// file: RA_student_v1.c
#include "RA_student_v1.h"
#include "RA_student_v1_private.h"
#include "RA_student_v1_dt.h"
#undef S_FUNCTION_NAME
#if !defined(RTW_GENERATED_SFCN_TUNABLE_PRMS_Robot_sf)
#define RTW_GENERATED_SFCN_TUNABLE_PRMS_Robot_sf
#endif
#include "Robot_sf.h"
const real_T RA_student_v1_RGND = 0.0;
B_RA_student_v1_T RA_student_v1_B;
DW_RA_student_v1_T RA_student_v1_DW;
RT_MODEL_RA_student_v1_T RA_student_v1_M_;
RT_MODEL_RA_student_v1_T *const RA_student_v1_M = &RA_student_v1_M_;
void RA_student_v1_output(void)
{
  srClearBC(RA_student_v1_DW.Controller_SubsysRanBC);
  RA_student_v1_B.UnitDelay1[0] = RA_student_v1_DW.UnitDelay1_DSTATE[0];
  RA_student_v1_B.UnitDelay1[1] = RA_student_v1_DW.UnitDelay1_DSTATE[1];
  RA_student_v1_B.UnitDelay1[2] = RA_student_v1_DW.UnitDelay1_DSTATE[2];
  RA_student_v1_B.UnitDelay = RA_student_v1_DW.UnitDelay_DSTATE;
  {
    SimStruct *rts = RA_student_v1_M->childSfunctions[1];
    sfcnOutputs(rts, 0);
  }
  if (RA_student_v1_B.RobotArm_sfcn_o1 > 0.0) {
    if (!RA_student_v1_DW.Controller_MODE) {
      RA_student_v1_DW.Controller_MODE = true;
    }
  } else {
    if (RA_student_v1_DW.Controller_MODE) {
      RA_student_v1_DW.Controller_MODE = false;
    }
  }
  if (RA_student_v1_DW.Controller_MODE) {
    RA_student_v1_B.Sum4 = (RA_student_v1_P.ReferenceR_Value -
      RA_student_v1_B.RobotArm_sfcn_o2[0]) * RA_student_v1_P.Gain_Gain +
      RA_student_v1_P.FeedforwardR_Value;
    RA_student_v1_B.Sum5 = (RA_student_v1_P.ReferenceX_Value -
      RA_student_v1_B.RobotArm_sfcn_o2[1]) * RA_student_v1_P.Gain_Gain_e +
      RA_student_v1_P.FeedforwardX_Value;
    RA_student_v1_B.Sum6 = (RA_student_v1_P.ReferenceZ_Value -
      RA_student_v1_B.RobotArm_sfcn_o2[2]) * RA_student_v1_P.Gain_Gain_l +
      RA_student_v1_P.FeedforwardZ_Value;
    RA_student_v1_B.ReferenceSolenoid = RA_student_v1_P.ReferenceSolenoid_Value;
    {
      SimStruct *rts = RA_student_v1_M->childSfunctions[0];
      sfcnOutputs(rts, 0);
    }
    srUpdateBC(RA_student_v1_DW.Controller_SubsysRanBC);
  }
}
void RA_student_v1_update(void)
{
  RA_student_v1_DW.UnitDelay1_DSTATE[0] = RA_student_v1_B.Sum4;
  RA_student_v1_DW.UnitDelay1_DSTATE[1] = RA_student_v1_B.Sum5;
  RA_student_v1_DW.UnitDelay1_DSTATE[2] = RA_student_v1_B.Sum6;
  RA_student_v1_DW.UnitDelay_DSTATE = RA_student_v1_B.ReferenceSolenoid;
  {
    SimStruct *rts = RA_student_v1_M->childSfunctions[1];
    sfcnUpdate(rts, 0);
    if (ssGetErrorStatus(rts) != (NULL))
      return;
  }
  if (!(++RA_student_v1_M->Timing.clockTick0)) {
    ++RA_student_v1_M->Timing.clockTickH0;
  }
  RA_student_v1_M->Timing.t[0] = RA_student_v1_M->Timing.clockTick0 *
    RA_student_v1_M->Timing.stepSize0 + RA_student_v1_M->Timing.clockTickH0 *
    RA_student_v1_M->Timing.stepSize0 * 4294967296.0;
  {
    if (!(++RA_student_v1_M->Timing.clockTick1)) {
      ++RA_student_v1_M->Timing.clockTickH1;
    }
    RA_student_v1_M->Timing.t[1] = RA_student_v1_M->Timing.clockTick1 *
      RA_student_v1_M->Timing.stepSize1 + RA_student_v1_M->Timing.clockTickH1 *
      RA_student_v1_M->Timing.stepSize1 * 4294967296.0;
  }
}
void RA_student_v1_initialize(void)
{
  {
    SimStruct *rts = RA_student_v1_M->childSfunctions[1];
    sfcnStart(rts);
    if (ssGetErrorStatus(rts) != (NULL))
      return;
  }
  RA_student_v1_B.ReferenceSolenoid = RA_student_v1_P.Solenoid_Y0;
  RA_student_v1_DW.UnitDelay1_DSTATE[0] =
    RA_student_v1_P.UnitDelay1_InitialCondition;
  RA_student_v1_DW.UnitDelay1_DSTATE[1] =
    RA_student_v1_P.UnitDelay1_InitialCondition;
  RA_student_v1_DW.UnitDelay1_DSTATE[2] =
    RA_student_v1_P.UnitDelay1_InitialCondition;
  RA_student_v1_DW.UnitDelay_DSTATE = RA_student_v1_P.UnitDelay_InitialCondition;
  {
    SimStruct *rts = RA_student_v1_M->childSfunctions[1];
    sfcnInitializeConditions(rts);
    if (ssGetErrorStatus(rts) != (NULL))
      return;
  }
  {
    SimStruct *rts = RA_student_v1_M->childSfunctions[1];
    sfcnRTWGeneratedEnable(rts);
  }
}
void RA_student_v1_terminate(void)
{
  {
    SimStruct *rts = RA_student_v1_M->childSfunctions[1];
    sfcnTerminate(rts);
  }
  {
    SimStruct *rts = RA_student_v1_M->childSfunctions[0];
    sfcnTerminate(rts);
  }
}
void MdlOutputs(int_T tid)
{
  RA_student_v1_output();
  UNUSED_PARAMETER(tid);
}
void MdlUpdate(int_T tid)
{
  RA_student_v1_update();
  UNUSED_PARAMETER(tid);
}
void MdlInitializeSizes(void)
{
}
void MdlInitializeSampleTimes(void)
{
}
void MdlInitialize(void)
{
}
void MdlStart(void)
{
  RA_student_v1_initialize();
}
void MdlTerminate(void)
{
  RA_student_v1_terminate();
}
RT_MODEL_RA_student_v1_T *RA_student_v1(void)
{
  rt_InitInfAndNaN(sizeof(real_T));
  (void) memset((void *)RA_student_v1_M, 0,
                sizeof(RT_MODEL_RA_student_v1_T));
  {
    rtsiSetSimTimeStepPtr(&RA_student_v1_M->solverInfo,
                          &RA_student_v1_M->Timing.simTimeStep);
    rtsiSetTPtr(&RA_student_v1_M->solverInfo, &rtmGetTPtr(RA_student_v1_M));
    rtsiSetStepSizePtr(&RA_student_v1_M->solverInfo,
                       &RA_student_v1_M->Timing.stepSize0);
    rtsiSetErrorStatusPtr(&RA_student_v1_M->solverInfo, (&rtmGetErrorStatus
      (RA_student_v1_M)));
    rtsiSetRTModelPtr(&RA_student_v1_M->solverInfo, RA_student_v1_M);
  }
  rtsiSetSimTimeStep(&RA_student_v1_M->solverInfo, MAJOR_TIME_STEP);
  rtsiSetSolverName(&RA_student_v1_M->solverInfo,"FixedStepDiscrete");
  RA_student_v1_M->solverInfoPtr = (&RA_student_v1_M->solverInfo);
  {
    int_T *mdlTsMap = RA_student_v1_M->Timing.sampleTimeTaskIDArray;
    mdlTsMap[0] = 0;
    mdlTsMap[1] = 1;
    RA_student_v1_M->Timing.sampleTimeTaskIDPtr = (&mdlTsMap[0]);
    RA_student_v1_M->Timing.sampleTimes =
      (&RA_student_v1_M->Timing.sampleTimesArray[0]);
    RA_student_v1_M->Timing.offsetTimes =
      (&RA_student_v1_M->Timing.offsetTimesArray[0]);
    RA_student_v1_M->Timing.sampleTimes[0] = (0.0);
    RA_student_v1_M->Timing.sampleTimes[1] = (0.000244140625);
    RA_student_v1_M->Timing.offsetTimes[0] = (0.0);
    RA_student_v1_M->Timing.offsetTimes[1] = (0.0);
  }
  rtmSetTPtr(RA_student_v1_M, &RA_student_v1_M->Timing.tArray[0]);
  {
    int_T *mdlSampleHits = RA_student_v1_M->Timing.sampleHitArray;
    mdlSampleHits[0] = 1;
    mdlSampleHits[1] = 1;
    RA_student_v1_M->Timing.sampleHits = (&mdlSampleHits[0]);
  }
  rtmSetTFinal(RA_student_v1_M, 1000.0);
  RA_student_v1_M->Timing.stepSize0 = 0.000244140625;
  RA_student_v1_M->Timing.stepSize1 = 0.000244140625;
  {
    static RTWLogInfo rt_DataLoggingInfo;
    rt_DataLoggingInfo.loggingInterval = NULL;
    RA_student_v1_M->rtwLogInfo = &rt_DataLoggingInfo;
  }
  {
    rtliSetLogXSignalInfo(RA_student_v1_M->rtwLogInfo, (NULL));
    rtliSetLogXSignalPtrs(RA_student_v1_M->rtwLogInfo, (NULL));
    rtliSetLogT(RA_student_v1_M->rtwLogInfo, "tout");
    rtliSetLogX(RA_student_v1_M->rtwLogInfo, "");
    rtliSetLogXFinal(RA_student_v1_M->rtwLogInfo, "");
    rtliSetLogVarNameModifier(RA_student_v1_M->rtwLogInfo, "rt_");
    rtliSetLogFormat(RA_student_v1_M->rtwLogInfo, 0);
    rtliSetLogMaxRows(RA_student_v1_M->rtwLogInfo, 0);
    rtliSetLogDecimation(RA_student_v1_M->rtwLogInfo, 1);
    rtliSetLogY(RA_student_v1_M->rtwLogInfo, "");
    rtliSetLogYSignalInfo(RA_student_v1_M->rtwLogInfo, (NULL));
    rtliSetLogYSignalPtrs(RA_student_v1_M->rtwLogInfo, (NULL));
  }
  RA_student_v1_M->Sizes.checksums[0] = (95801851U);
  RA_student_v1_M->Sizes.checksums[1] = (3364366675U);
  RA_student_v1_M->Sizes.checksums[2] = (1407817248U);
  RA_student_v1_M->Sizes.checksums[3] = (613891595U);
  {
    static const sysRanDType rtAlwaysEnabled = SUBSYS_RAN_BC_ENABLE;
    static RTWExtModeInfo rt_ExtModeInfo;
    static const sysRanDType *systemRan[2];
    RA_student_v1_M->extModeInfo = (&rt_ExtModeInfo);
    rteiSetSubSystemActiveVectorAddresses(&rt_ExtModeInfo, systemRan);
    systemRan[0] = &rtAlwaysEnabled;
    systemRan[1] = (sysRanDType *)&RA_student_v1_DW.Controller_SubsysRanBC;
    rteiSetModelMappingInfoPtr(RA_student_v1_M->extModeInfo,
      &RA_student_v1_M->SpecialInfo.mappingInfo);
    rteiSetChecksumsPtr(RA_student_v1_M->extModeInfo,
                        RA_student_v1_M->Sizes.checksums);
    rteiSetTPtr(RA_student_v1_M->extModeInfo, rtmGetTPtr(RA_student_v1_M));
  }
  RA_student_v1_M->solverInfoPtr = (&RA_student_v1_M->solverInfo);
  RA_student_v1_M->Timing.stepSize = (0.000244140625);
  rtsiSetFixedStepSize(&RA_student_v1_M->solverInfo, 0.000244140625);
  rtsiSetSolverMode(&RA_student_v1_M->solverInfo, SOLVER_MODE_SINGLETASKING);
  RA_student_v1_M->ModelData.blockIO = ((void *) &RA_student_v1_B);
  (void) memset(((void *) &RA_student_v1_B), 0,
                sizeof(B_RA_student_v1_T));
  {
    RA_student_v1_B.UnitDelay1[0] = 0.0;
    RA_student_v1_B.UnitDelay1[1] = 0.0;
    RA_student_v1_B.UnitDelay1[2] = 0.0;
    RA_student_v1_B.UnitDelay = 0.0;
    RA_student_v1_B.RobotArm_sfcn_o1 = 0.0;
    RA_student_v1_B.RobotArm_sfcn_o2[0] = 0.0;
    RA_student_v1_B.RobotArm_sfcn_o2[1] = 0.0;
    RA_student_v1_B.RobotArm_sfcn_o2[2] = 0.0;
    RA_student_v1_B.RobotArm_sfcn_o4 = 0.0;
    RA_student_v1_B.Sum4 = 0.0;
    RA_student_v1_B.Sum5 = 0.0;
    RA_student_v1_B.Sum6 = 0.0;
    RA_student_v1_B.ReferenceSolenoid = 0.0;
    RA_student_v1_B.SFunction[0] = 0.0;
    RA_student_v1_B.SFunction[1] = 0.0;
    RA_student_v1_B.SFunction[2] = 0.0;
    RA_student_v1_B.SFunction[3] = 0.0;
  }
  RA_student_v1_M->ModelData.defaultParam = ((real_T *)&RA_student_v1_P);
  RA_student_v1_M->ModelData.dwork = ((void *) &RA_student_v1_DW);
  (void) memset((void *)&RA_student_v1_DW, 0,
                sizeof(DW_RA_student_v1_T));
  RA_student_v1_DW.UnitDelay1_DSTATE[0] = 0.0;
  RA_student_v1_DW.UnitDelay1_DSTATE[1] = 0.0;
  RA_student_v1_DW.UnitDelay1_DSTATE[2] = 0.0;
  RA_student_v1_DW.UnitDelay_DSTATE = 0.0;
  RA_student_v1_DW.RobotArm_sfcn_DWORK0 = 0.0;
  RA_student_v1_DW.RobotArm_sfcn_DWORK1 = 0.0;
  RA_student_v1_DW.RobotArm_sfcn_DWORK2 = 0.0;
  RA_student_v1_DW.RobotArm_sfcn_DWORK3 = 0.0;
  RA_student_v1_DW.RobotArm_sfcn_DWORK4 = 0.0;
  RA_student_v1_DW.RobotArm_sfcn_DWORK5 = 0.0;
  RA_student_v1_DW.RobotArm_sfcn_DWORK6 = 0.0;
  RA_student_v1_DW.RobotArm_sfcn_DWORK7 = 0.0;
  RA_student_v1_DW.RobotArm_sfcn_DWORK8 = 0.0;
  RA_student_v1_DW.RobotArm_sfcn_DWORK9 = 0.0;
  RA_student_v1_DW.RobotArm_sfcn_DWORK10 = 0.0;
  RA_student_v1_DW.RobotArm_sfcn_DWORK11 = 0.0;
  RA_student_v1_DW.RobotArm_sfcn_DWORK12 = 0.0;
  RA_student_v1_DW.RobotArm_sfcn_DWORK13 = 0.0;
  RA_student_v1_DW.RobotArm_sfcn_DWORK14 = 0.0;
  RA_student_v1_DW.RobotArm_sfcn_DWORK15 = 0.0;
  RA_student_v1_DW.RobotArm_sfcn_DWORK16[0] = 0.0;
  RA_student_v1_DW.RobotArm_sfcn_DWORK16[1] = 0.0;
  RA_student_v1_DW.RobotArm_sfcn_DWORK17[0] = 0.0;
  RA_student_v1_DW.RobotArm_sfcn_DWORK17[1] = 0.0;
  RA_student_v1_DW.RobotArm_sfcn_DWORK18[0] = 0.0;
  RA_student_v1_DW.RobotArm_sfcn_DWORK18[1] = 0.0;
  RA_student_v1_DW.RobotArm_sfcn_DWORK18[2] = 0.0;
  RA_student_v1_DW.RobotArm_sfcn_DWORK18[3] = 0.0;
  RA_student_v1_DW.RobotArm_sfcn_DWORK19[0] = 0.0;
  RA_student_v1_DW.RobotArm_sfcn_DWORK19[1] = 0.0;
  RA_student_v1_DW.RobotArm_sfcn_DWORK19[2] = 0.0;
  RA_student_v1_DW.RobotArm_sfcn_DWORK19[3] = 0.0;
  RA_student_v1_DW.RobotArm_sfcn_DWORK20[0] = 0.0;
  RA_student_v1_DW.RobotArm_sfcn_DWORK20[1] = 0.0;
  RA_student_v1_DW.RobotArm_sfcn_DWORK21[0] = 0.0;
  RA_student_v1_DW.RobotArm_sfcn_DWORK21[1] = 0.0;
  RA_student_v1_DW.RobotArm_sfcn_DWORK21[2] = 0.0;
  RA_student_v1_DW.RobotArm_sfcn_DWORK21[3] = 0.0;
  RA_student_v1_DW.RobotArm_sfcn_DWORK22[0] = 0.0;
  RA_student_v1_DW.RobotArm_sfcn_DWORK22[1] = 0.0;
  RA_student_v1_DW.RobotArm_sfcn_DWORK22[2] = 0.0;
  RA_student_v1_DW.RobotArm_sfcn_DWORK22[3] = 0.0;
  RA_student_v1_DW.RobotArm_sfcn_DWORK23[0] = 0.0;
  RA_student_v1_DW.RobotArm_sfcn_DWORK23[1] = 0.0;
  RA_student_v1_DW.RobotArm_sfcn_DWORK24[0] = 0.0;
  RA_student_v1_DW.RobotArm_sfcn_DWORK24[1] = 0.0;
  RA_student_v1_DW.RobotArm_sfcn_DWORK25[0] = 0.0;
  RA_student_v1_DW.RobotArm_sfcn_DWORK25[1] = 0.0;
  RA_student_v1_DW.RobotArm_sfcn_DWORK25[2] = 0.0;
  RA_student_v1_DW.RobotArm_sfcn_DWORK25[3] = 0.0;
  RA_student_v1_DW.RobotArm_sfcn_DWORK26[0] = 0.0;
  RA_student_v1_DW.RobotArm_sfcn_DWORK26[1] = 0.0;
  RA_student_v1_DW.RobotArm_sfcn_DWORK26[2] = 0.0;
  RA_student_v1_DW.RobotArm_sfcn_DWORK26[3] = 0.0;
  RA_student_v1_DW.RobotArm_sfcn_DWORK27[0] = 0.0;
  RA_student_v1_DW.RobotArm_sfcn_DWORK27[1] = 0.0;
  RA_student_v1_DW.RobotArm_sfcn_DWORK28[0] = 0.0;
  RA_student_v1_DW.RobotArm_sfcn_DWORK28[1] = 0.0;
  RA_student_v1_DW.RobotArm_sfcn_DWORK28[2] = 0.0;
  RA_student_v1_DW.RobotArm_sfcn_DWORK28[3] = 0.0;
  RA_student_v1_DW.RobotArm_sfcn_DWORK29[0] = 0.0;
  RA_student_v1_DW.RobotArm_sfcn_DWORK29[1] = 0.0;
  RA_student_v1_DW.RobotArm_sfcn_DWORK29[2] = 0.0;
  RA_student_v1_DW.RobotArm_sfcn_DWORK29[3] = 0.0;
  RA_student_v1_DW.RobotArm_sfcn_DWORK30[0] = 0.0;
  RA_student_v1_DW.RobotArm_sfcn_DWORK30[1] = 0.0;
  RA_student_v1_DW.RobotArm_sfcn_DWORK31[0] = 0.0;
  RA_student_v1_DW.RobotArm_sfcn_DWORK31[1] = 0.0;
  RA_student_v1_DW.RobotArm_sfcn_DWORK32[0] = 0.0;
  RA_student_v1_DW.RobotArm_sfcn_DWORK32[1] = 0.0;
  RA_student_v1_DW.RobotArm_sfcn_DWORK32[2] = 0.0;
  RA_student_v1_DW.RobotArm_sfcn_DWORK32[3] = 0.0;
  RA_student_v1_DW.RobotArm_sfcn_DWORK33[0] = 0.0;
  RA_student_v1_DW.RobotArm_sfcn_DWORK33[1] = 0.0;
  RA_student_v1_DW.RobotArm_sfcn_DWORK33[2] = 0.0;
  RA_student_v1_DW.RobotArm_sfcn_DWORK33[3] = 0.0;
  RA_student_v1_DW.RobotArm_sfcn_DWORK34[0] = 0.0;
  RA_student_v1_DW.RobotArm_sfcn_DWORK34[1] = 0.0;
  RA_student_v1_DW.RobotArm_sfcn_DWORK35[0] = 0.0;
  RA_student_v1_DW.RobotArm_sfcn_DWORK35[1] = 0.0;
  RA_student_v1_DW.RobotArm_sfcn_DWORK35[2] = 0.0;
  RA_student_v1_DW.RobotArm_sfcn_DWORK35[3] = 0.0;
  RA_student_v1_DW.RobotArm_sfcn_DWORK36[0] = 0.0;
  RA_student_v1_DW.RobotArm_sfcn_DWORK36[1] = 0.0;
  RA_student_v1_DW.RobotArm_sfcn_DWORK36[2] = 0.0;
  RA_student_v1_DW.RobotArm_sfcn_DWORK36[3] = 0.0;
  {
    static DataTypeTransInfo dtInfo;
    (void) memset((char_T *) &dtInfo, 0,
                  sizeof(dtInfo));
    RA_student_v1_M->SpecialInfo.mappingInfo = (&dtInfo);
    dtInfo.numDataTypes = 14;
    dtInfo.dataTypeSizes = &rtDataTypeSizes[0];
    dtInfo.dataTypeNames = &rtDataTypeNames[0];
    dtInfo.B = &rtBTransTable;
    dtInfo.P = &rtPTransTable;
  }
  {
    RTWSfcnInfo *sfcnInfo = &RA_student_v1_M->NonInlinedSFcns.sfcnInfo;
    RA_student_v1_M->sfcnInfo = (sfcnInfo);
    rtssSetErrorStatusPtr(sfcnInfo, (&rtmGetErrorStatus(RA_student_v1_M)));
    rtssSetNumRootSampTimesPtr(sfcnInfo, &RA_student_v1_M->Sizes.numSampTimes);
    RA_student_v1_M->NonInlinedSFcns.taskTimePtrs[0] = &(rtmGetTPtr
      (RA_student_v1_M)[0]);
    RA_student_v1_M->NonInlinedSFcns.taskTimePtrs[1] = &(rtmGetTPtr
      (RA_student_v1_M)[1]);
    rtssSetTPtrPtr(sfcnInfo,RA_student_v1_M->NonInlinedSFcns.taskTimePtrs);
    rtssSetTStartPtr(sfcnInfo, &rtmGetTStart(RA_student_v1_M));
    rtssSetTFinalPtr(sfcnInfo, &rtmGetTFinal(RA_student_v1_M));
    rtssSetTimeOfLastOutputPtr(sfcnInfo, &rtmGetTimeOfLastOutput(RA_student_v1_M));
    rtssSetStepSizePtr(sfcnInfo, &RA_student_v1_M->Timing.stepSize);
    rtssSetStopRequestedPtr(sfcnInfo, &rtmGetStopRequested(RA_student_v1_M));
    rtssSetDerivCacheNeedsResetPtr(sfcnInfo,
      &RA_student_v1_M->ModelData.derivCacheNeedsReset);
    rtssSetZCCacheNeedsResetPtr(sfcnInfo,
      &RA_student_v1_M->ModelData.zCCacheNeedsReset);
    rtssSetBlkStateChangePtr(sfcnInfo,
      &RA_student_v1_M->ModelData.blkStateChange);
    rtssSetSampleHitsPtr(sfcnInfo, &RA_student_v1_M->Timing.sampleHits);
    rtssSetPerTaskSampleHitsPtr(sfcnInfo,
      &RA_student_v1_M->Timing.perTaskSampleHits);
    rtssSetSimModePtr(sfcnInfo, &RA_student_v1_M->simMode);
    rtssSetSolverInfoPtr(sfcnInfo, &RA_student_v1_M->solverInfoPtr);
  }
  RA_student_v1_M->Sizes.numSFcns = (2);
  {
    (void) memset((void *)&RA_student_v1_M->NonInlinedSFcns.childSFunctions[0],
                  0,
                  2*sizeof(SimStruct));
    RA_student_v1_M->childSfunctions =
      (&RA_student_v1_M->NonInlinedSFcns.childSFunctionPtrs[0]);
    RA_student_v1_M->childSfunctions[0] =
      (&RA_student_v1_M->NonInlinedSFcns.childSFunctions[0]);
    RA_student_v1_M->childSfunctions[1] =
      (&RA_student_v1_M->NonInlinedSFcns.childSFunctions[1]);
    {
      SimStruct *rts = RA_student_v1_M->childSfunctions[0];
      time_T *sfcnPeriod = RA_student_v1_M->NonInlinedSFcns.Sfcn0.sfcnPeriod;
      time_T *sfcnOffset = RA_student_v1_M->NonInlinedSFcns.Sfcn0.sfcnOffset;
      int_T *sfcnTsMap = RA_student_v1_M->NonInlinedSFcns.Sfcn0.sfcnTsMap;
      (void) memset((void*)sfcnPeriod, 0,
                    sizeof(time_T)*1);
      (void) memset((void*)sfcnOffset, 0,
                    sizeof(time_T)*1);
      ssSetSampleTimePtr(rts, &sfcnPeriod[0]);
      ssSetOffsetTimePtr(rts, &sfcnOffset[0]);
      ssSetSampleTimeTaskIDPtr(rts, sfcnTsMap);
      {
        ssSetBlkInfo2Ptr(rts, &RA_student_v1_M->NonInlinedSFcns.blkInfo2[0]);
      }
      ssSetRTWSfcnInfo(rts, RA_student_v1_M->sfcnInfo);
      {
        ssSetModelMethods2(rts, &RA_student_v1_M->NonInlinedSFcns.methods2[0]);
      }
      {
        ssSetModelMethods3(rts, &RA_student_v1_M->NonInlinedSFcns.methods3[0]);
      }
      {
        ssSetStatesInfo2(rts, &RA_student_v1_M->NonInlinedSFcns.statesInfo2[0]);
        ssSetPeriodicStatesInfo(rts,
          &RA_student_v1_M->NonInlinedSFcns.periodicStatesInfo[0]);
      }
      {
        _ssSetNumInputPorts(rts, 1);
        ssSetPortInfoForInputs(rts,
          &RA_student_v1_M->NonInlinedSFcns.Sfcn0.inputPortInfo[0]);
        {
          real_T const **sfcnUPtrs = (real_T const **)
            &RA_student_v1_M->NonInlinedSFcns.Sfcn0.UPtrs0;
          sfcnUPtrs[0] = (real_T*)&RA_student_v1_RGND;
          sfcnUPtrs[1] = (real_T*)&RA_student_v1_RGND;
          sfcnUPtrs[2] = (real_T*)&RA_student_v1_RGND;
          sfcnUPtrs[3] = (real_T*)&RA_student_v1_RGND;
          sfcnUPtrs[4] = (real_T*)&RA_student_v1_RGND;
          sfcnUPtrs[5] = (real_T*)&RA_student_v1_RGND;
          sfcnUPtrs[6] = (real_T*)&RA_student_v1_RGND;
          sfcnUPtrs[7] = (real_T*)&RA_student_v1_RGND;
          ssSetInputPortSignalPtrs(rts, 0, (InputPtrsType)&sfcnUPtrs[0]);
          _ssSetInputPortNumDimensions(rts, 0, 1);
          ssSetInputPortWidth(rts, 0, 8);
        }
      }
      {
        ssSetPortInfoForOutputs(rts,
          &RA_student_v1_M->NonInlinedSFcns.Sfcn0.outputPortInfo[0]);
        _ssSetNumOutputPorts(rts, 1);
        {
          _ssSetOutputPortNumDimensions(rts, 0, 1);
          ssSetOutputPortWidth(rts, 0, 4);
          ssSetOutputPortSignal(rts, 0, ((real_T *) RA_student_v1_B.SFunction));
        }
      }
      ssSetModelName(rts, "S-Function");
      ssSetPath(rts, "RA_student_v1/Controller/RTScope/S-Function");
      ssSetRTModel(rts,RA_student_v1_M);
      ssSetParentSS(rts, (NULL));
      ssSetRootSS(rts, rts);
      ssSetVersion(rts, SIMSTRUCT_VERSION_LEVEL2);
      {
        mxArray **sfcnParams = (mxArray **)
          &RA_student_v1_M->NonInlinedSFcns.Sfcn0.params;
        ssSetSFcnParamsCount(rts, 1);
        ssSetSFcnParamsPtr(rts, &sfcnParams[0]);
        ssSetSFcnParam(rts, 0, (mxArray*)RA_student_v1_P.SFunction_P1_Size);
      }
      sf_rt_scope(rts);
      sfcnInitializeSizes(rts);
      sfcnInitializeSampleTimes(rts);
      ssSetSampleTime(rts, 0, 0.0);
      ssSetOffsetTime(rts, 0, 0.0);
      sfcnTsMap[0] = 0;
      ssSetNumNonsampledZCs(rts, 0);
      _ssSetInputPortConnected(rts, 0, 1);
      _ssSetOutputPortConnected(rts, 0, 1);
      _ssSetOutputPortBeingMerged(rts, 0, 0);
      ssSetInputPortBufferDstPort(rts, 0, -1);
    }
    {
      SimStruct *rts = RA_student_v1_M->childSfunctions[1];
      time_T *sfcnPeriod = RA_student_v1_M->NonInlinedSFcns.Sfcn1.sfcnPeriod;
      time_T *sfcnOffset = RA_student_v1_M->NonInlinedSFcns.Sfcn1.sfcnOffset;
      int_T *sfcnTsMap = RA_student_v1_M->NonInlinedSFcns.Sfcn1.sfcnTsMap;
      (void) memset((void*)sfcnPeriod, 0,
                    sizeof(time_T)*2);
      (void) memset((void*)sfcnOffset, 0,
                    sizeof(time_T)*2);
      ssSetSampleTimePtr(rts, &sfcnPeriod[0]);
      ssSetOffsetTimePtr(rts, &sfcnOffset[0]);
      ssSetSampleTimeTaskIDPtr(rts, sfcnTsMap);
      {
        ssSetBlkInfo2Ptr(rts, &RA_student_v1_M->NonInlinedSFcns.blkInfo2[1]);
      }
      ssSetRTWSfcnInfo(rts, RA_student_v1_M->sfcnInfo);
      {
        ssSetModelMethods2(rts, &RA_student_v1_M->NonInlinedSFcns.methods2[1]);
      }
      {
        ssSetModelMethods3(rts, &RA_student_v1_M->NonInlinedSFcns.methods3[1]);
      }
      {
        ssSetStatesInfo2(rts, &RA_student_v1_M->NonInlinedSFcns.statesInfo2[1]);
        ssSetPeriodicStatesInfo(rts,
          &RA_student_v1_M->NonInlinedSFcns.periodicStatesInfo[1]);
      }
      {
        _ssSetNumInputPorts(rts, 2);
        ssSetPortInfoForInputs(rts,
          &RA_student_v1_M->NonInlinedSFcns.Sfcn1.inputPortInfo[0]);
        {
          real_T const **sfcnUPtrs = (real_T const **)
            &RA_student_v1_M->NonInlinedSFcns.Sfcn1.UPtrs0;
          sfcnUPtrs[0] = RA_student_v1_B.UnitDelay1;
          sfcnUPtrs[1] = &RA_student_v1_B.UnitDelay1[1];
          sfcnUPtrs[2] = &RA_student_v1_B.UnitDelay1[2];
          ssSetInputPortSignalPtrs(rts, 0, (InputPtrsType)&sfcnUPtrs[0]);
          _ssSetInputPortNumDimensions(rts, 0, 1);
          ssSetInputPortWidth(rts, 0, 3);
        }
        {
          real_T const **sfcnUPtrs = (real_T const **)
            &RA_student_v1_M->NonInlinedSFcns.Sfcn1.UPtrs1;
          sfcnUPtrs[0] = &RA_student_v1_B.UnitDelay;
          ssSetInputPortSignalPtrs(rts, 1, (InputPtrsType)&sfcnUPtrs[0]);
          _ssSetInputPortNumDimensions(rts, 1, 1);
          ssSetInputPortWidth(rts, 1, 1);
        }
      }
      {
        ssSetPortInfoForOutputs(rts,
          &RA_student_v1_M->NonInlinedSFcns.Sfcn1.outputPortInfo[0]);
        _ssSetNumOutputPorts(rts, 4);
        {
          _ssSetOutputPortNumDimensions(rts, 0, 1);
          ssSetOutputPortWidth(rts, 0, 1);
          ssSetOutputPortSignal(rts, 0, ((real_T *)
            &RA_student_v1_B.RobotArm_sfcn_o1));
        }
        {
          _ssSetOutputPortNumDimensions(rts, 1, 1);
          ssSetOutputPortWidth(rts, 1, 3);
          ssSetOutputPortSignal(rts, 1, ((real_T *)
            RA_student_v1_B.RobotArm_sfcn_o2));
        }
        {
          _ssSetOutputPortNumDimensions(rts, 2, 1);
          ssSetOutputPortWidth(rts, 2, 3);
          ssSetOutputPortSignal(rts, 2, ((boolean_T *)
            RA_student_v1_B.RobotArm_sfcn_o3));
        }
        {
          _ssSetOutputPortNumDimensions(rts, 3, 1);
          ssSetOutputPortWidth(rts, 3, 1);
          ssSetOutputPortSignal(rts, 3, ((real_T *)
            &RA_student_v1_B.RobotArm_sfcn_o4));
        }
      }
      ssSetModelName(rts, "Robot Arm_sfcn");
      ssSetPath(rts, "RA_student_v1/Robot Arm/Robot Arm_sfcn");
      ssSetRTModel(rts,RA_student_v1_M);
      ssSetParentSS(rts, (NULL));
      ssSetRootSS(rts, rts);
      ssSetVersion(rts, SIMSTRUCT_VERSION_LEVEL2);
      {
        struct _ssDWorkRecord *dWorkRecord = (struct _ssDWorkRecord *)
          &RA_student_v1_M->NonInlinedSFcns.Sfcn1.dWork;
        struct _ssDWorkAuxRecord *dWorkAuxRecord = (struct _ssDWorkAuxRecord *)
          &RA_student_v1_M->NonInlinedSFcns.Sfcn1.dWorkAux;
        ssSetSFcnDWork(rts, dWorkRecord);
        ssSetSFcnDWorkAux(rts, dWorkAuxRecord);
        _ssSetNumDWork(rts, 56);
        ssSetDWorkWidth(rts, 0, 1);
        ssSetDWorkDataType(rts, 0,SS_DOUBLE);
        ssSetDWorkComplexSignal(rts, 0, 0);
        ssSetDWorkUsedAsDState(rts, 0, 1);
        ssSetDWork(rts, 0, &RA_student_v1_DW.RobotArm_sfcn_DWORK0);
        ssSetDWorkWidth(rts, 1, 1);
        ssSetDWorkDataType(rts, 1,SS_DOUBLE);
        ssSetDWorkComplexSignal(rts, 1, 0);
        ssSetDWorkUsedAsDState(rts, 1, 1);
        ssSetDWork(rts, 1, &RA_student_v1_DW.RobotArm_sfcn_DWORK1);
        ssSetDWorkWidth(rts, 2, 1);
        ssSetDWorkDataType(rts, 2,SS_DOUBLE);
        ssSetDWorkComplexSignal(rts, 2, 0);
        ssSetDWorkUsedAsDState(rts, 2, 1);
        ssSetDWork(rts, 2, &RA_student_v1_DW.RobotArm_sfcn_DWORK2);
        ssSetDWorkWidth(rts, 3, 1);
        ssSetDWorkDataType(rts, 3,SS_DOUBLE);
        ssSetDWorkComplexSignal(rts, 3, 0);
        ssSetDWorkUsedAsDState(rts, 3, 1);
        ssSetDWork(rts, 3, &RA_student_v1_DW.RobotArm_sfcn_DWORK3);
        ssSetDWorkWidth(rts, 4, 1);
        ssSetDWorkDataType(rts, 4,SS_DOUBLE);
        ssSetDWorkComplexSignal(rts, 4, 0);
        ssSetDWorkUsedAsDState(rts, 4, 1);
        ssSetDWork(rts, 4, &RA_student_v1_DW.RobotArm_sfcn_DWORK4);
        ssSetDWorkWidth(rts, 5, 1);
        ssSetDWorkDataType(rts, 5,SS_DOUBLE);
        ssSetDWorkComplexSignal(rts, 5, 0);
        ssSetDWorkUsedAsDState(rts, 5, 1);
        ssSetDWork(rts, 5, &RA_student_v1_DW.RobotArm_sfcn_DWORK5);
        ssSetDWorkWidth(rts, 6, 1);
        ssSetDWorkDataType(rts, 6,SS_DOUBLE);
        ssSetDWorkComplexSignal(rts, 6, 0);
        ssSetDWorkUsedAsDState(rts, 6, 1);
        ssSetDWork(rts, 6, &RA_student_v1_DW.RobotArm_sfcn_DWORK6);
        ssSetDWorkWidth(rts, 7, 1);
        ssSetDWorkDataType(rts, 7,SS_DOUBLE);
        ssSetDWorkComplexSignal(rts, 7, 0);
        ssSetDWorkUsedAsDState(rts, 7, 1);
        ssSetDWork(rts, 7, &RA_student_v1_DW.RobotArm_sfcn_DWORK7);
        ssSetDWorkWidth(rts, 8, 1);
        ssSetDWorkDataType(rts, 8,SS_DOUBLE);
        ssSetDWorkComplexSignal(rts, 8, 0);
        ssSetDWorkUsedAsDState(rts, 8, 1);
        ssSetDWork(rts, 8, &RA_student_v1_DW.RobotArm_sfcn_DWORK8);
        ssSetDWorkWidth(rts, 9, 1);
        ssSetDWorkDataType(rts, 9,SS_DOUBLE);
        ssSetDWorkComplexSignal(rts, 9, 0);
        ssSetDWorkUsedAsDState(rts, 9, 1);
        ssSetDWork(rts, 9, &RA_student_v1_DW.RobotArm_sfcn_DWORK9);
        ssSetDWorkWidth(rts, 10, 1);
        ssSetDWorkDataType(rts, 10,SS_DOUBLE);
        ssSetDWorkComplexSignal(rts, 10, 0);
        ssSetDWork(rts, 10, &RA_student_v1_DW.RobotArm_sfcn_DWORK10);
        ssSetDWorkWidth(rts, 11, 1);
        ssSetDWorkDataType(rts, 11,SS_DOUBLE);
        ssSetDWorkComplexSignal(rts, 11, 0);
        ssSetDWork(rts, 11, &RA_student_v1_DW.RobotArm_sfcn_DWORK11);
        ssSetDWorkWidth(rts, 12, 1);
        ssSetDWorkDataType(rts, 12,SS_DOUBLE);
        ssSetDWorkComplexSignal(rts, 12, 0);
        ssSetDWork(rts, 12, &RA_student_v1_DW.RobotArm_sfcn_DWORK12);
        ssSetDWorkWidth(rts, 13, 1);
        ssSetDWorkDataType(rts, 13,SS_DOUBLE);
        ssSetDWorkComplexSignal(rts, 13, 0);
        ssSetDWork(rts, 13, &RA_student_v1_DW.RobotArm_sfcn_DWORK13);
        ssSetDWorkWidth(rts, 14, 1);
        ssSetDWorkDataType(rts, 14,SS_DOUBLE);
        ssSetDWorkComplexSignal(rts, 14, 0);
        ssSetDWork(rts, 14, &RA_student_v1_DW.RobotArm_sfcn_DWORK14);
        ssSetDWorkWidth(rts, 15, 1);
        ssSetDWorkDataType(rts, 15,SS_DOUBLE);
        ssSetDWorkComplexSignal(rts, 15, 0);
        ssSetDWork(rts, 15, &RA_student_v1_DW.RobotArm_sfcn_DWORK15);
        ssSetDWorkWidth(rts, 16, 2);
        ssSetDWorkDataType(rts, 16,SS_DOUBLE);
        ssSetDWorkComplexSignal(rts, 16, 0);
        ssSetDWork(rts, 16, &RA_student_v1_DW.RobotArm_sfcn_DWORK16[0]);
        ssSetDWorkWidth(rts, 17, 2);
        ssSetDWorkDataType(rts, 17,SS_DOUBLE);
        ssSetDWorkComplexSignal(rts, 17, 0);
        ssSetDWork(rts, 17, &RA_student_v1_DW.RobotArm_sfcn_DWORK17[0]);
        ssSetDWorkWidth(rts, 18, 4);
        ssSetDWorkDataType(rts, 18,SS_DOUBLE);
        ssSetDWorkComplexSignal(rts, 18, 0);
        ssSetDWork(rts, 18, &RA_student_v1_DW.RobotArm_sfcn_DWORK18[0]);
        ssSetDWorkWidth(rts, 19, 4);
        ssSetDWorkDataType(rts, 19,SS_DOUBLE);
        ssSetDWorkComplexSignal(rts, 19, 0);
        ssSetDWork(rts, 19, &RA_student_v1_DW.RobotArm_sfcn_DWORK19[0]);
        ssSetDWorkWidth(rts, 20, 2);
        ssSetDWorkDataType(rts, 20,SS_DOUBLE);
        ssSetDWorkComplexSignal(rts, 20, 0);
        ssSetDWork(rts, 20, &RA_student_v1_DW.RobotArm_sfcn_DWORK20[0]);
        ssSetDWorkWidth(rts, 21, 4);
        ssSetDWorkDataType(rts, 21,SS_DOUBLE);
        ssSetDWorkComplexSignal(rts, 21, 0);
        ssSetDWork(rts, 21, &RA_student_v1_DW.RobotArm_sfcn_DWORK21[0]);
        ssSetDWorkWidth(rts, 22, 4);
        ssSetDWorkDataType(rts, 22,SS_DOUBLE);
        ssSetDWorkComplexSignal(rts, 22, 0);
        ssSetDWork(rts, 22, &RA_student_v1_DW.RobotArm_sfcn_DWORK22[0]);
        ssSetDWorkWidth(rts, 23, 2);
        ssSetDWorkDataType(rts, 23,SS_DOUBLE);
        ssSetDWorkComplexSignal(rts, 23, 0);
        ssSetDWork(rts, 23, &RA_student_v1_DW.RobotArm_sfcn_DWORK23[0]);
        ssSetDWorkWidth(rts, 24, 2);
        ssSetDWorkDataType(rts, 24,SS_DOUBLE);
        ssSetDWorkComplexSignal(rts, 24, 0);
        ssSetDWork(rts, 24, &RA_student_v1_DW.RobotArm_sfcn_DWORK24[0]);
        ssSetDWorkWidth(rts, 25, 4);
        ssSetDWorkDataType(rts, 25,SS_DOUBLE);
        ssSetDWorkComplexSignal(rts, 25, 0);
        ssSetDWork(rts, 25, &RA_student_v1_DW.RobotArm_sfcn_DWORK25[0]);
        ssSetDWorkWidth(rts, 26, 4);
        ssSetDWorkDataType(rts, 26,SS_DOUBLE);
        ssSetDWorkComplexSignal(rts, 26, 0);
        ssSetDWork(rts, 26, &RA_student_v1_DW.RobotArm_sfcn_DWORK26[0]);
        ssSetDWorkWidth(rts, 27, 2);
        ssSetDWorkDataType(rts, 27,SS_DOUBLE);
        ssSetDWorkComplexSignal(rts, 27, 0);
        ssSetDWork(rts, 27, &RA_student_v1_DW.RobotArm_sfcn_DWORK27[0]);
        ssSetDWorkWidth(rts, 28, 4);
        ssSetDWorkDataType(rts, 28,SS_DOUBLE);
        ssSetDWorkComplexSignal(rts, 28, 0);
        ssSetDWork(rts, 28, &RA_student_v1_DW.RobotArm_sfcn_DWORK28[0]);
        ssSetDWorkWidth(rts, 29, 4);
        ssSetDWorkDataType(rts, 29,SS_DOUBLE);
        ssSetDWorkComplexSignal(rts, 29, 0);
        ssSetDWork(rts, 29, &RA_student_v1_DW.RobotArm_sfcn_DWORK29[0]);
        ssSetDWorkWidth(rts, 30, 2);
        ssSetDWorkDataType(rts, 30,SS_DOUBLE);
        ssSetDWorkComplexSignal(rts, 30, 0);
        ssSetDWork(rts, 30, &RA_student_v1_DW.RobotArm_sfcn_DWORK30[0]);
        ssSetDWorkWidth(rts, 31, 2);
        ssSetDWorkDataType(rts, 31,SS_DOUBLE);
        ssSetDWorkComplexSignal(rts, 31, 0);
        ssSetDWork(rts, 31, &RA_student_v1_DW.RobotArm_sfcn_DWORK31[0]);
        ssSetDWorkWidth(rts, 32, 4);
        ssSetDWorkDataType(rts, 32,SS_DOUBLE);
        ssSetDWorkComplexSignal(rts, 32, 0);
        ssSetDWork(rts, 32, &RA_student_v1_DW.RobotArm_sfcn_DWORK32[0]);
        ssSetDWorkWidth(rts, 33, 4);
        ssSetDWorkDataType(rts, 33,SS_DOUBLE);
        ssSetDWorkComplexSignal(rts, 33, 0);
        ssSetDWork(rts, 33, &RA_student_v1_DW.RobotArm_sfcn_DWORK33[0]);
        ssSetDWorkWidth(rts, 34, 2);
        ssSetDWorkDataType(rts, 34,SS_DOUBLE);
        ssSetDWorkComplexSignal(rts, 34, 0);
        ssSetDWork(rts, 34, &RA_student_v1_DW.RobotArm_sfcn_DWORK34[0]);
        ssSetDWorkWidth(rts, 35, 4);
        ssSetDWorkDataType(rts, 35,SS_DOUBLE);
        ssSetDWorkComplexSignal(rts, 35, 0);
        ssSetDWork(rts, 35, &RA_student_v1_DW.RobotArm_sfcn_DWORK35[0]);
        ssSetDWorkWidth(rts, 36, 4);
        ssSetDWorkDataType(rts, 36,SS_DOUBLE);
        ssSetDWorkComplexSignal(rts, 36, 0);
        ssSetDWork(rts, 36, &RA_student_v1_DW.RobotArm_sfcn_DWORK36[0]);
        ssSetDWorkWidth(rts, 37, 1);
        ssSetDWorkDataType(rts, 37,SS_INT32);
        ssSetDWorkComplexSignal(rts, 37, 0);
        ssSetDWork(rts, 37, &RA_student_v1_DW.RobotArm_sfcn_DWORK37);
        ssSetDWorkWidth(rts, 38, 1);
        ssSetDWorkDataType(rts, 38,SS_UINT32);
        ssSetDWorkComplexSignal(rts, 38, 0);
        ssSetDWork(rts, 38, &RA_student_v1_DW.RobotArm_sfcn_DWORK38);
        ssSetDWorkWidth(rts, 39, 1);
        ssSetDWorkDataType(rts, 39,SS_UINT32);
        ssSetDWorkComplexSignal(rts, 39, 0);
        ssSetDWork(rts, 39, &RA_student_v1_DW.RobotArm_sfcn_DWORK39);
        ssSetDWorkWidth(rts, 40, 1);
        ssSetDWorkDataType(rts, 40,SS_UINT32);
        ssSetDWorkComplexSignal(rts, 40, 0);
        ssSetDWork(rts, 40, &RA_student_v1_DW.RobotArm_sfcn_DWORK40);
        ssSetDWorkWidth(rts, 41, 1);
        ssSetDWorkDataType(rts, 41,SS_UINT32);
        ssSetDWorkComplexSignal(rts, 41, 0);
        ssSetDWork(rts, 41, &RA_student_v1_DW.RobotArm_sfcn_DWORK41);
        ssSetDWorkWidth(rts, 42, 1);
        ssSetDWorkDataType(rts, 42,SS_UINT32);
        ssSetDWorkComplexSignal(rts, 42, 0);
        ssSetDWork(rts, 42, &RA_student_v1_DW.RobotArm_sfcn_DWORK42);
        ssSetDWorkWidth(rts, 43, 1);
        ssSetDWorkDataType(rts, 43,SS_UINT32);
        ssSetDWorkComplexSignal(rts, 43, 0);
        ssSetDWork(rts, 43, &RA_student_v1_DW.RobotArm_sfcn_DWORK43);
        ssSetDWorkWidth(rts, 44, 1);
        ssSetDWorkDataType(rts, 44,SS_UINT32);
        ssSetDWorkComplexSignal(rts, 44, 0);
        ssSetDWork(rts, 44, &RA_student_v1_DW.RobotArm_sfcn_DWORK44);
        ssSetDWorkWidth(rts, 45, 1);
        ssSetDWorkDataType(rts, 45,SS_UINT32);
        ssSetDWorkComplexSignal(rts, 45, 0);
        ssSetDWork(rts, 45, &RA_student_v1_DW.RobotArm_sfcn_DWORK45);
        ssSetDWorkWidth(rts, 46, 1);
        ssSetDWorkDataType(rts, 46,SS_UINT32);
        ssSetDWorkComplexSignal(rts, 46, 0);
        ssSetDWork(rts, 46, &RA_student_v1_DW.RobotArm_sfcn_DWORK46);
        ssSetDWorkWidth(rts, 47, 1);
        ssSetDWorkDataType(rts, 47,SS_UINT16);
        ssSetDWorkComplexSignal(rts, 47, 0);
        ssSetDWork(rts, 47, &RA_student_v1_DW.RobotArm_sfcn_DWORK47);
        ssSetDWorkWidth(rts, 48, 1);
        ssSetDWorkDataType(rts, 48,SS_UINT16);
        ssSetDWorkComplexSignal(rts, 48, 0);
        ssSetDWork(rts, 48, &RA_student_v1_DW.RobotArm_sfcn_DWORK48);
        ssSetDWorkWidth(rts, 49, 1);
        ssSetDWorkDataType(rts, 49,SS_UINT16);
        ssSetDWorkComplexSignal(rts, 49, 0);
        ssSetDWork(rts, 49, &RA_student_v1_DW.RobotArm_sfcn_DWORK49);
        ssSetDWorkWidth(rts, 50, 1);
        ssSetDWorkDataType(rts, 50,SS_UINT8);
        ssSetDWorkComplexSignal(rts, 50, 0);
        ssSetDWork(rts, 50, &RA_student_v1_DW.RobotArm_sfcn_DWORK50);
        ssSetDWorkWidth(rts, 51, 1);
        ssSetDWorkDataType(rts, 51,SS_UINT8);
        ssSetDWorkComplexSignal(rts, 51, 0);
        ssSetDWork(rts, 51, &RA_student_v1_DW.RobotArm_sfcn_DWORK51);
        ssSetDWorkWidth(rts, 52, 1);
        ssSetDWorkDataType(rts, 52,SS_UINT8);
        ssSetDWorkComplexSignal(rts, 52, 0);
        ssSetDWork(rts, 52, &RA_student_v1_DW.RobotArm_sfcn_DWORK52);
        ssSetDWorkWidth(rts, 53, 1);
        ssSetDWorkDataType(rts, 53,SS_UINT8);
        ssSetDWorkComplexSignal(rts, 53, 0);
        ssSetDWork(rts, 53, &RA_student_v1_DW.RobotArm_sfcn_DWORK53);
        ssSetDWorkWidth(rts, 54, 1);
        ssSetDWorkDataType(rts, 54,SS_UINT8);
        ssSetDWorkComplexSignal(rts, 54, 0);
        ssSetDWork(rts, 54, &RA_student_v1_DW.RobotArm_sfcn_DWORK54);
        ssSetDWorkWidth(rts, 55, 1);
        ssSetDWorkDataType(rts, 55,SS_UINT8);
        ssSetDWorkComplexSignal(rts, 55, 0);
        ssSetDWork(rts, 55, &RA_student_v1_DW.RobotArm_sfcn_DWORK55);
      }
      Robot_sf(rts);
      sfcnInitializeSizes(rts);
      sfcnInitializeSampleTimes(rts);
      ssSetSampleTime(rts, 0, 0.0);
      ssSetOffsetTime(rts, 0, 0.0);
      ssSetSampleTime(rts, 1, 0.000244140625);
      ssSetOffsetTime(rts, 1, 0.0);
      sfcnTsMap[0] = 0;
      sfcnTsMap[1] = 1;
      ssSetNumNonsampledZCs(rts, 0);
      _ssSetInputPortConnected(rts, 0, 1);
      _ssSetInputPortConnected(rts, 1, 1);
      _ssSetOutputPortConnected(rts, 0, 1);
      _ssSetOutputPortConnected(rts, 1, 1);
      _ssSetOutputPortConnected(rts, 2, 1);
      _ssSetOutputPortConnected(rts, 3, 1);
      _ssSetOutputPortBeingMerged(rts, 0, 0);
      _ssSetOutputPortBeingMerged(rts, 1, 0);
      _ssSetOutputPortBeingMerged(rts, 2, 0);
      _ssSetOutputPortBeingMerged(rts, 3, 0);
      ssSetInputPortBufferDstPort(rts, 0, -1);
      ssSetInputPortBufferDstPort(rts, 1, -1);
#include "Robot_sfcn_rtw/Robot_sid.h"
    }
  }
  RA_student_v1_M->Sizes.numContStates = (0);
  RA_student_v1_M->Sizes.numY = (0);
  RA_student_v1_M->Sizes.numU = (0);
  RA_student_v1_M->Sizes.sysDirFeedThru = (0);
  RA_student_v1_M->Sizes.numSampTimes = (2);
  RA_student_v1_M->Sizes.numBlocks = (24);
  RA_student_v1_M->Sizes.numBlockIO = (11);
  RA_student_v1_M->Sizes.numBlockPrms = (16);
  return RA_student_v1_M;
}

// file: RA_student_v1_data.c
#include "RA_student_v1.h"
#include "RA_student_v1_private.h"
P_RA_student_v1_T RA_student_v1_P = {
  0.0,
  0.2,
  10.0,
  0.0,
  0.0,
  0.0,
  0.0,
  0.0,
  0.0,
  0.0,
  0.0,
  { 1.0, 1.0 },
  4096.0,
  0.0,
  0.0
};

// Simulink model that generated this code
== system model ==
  UnitDelay1 : UnitDelay  <- 1: Controller
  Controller : Subsystem  <- 1: RobotArm_sfcn/2, Enable: RobotArm_sfcn
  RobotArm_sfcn : S-Function  FunctionName=Robot_sf  <- 1: UnitDelay1, 2: UnitDelay
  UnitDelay : UnitDelay  <- 1: Controller/2
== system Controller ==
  Inport#1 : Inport
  EnablePort#1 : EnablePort
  Outport#1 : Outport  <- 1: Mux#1
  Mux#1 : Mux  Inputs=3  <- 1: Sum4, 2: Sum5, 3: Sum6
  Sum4 : Sum  Inputs=++  <- 1: FeedforwardR, 2: Gain
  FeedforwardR : Constant  Value=0
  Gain : Gain  Gain=10  <- 1: Sum#1
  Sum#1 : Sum  Inputs=+-  <- 1: ReferenceR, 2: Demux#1
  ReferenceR : Constant  Value=0.2
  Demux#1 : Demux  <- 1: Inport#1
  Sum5 : Sum  Inputs=++  <- 1: FeedforwardX, 2: Gain#1
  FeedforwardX : Constant  Value=0
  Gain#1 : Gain  Gain=0  <- 1: Sum#2
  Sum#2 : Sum  Inputs=+-  <- 1: ReferenceX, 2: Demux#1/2
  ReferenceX : Constant  Value=0
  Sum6 : Sum  Inputs=++  <- 1: FeedforwardZ, 2: Gain#2
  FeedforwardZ : Constant  Value=0
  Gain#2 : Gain  Gain=0  <- 1: Sum#3
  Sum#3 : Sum  Inputs=+-  <- 1: ReferenceZ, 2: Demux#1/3
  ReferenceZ : Constant  Value=0
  Solenoid : Outport  InitialOutput=0  <- 1: ReferenceSolenoid
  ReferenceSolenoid : Constant  Value=0
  SFunction : S-Function  FunctionName=sf_rt_scope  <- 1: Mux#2
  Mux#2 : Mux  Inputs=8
